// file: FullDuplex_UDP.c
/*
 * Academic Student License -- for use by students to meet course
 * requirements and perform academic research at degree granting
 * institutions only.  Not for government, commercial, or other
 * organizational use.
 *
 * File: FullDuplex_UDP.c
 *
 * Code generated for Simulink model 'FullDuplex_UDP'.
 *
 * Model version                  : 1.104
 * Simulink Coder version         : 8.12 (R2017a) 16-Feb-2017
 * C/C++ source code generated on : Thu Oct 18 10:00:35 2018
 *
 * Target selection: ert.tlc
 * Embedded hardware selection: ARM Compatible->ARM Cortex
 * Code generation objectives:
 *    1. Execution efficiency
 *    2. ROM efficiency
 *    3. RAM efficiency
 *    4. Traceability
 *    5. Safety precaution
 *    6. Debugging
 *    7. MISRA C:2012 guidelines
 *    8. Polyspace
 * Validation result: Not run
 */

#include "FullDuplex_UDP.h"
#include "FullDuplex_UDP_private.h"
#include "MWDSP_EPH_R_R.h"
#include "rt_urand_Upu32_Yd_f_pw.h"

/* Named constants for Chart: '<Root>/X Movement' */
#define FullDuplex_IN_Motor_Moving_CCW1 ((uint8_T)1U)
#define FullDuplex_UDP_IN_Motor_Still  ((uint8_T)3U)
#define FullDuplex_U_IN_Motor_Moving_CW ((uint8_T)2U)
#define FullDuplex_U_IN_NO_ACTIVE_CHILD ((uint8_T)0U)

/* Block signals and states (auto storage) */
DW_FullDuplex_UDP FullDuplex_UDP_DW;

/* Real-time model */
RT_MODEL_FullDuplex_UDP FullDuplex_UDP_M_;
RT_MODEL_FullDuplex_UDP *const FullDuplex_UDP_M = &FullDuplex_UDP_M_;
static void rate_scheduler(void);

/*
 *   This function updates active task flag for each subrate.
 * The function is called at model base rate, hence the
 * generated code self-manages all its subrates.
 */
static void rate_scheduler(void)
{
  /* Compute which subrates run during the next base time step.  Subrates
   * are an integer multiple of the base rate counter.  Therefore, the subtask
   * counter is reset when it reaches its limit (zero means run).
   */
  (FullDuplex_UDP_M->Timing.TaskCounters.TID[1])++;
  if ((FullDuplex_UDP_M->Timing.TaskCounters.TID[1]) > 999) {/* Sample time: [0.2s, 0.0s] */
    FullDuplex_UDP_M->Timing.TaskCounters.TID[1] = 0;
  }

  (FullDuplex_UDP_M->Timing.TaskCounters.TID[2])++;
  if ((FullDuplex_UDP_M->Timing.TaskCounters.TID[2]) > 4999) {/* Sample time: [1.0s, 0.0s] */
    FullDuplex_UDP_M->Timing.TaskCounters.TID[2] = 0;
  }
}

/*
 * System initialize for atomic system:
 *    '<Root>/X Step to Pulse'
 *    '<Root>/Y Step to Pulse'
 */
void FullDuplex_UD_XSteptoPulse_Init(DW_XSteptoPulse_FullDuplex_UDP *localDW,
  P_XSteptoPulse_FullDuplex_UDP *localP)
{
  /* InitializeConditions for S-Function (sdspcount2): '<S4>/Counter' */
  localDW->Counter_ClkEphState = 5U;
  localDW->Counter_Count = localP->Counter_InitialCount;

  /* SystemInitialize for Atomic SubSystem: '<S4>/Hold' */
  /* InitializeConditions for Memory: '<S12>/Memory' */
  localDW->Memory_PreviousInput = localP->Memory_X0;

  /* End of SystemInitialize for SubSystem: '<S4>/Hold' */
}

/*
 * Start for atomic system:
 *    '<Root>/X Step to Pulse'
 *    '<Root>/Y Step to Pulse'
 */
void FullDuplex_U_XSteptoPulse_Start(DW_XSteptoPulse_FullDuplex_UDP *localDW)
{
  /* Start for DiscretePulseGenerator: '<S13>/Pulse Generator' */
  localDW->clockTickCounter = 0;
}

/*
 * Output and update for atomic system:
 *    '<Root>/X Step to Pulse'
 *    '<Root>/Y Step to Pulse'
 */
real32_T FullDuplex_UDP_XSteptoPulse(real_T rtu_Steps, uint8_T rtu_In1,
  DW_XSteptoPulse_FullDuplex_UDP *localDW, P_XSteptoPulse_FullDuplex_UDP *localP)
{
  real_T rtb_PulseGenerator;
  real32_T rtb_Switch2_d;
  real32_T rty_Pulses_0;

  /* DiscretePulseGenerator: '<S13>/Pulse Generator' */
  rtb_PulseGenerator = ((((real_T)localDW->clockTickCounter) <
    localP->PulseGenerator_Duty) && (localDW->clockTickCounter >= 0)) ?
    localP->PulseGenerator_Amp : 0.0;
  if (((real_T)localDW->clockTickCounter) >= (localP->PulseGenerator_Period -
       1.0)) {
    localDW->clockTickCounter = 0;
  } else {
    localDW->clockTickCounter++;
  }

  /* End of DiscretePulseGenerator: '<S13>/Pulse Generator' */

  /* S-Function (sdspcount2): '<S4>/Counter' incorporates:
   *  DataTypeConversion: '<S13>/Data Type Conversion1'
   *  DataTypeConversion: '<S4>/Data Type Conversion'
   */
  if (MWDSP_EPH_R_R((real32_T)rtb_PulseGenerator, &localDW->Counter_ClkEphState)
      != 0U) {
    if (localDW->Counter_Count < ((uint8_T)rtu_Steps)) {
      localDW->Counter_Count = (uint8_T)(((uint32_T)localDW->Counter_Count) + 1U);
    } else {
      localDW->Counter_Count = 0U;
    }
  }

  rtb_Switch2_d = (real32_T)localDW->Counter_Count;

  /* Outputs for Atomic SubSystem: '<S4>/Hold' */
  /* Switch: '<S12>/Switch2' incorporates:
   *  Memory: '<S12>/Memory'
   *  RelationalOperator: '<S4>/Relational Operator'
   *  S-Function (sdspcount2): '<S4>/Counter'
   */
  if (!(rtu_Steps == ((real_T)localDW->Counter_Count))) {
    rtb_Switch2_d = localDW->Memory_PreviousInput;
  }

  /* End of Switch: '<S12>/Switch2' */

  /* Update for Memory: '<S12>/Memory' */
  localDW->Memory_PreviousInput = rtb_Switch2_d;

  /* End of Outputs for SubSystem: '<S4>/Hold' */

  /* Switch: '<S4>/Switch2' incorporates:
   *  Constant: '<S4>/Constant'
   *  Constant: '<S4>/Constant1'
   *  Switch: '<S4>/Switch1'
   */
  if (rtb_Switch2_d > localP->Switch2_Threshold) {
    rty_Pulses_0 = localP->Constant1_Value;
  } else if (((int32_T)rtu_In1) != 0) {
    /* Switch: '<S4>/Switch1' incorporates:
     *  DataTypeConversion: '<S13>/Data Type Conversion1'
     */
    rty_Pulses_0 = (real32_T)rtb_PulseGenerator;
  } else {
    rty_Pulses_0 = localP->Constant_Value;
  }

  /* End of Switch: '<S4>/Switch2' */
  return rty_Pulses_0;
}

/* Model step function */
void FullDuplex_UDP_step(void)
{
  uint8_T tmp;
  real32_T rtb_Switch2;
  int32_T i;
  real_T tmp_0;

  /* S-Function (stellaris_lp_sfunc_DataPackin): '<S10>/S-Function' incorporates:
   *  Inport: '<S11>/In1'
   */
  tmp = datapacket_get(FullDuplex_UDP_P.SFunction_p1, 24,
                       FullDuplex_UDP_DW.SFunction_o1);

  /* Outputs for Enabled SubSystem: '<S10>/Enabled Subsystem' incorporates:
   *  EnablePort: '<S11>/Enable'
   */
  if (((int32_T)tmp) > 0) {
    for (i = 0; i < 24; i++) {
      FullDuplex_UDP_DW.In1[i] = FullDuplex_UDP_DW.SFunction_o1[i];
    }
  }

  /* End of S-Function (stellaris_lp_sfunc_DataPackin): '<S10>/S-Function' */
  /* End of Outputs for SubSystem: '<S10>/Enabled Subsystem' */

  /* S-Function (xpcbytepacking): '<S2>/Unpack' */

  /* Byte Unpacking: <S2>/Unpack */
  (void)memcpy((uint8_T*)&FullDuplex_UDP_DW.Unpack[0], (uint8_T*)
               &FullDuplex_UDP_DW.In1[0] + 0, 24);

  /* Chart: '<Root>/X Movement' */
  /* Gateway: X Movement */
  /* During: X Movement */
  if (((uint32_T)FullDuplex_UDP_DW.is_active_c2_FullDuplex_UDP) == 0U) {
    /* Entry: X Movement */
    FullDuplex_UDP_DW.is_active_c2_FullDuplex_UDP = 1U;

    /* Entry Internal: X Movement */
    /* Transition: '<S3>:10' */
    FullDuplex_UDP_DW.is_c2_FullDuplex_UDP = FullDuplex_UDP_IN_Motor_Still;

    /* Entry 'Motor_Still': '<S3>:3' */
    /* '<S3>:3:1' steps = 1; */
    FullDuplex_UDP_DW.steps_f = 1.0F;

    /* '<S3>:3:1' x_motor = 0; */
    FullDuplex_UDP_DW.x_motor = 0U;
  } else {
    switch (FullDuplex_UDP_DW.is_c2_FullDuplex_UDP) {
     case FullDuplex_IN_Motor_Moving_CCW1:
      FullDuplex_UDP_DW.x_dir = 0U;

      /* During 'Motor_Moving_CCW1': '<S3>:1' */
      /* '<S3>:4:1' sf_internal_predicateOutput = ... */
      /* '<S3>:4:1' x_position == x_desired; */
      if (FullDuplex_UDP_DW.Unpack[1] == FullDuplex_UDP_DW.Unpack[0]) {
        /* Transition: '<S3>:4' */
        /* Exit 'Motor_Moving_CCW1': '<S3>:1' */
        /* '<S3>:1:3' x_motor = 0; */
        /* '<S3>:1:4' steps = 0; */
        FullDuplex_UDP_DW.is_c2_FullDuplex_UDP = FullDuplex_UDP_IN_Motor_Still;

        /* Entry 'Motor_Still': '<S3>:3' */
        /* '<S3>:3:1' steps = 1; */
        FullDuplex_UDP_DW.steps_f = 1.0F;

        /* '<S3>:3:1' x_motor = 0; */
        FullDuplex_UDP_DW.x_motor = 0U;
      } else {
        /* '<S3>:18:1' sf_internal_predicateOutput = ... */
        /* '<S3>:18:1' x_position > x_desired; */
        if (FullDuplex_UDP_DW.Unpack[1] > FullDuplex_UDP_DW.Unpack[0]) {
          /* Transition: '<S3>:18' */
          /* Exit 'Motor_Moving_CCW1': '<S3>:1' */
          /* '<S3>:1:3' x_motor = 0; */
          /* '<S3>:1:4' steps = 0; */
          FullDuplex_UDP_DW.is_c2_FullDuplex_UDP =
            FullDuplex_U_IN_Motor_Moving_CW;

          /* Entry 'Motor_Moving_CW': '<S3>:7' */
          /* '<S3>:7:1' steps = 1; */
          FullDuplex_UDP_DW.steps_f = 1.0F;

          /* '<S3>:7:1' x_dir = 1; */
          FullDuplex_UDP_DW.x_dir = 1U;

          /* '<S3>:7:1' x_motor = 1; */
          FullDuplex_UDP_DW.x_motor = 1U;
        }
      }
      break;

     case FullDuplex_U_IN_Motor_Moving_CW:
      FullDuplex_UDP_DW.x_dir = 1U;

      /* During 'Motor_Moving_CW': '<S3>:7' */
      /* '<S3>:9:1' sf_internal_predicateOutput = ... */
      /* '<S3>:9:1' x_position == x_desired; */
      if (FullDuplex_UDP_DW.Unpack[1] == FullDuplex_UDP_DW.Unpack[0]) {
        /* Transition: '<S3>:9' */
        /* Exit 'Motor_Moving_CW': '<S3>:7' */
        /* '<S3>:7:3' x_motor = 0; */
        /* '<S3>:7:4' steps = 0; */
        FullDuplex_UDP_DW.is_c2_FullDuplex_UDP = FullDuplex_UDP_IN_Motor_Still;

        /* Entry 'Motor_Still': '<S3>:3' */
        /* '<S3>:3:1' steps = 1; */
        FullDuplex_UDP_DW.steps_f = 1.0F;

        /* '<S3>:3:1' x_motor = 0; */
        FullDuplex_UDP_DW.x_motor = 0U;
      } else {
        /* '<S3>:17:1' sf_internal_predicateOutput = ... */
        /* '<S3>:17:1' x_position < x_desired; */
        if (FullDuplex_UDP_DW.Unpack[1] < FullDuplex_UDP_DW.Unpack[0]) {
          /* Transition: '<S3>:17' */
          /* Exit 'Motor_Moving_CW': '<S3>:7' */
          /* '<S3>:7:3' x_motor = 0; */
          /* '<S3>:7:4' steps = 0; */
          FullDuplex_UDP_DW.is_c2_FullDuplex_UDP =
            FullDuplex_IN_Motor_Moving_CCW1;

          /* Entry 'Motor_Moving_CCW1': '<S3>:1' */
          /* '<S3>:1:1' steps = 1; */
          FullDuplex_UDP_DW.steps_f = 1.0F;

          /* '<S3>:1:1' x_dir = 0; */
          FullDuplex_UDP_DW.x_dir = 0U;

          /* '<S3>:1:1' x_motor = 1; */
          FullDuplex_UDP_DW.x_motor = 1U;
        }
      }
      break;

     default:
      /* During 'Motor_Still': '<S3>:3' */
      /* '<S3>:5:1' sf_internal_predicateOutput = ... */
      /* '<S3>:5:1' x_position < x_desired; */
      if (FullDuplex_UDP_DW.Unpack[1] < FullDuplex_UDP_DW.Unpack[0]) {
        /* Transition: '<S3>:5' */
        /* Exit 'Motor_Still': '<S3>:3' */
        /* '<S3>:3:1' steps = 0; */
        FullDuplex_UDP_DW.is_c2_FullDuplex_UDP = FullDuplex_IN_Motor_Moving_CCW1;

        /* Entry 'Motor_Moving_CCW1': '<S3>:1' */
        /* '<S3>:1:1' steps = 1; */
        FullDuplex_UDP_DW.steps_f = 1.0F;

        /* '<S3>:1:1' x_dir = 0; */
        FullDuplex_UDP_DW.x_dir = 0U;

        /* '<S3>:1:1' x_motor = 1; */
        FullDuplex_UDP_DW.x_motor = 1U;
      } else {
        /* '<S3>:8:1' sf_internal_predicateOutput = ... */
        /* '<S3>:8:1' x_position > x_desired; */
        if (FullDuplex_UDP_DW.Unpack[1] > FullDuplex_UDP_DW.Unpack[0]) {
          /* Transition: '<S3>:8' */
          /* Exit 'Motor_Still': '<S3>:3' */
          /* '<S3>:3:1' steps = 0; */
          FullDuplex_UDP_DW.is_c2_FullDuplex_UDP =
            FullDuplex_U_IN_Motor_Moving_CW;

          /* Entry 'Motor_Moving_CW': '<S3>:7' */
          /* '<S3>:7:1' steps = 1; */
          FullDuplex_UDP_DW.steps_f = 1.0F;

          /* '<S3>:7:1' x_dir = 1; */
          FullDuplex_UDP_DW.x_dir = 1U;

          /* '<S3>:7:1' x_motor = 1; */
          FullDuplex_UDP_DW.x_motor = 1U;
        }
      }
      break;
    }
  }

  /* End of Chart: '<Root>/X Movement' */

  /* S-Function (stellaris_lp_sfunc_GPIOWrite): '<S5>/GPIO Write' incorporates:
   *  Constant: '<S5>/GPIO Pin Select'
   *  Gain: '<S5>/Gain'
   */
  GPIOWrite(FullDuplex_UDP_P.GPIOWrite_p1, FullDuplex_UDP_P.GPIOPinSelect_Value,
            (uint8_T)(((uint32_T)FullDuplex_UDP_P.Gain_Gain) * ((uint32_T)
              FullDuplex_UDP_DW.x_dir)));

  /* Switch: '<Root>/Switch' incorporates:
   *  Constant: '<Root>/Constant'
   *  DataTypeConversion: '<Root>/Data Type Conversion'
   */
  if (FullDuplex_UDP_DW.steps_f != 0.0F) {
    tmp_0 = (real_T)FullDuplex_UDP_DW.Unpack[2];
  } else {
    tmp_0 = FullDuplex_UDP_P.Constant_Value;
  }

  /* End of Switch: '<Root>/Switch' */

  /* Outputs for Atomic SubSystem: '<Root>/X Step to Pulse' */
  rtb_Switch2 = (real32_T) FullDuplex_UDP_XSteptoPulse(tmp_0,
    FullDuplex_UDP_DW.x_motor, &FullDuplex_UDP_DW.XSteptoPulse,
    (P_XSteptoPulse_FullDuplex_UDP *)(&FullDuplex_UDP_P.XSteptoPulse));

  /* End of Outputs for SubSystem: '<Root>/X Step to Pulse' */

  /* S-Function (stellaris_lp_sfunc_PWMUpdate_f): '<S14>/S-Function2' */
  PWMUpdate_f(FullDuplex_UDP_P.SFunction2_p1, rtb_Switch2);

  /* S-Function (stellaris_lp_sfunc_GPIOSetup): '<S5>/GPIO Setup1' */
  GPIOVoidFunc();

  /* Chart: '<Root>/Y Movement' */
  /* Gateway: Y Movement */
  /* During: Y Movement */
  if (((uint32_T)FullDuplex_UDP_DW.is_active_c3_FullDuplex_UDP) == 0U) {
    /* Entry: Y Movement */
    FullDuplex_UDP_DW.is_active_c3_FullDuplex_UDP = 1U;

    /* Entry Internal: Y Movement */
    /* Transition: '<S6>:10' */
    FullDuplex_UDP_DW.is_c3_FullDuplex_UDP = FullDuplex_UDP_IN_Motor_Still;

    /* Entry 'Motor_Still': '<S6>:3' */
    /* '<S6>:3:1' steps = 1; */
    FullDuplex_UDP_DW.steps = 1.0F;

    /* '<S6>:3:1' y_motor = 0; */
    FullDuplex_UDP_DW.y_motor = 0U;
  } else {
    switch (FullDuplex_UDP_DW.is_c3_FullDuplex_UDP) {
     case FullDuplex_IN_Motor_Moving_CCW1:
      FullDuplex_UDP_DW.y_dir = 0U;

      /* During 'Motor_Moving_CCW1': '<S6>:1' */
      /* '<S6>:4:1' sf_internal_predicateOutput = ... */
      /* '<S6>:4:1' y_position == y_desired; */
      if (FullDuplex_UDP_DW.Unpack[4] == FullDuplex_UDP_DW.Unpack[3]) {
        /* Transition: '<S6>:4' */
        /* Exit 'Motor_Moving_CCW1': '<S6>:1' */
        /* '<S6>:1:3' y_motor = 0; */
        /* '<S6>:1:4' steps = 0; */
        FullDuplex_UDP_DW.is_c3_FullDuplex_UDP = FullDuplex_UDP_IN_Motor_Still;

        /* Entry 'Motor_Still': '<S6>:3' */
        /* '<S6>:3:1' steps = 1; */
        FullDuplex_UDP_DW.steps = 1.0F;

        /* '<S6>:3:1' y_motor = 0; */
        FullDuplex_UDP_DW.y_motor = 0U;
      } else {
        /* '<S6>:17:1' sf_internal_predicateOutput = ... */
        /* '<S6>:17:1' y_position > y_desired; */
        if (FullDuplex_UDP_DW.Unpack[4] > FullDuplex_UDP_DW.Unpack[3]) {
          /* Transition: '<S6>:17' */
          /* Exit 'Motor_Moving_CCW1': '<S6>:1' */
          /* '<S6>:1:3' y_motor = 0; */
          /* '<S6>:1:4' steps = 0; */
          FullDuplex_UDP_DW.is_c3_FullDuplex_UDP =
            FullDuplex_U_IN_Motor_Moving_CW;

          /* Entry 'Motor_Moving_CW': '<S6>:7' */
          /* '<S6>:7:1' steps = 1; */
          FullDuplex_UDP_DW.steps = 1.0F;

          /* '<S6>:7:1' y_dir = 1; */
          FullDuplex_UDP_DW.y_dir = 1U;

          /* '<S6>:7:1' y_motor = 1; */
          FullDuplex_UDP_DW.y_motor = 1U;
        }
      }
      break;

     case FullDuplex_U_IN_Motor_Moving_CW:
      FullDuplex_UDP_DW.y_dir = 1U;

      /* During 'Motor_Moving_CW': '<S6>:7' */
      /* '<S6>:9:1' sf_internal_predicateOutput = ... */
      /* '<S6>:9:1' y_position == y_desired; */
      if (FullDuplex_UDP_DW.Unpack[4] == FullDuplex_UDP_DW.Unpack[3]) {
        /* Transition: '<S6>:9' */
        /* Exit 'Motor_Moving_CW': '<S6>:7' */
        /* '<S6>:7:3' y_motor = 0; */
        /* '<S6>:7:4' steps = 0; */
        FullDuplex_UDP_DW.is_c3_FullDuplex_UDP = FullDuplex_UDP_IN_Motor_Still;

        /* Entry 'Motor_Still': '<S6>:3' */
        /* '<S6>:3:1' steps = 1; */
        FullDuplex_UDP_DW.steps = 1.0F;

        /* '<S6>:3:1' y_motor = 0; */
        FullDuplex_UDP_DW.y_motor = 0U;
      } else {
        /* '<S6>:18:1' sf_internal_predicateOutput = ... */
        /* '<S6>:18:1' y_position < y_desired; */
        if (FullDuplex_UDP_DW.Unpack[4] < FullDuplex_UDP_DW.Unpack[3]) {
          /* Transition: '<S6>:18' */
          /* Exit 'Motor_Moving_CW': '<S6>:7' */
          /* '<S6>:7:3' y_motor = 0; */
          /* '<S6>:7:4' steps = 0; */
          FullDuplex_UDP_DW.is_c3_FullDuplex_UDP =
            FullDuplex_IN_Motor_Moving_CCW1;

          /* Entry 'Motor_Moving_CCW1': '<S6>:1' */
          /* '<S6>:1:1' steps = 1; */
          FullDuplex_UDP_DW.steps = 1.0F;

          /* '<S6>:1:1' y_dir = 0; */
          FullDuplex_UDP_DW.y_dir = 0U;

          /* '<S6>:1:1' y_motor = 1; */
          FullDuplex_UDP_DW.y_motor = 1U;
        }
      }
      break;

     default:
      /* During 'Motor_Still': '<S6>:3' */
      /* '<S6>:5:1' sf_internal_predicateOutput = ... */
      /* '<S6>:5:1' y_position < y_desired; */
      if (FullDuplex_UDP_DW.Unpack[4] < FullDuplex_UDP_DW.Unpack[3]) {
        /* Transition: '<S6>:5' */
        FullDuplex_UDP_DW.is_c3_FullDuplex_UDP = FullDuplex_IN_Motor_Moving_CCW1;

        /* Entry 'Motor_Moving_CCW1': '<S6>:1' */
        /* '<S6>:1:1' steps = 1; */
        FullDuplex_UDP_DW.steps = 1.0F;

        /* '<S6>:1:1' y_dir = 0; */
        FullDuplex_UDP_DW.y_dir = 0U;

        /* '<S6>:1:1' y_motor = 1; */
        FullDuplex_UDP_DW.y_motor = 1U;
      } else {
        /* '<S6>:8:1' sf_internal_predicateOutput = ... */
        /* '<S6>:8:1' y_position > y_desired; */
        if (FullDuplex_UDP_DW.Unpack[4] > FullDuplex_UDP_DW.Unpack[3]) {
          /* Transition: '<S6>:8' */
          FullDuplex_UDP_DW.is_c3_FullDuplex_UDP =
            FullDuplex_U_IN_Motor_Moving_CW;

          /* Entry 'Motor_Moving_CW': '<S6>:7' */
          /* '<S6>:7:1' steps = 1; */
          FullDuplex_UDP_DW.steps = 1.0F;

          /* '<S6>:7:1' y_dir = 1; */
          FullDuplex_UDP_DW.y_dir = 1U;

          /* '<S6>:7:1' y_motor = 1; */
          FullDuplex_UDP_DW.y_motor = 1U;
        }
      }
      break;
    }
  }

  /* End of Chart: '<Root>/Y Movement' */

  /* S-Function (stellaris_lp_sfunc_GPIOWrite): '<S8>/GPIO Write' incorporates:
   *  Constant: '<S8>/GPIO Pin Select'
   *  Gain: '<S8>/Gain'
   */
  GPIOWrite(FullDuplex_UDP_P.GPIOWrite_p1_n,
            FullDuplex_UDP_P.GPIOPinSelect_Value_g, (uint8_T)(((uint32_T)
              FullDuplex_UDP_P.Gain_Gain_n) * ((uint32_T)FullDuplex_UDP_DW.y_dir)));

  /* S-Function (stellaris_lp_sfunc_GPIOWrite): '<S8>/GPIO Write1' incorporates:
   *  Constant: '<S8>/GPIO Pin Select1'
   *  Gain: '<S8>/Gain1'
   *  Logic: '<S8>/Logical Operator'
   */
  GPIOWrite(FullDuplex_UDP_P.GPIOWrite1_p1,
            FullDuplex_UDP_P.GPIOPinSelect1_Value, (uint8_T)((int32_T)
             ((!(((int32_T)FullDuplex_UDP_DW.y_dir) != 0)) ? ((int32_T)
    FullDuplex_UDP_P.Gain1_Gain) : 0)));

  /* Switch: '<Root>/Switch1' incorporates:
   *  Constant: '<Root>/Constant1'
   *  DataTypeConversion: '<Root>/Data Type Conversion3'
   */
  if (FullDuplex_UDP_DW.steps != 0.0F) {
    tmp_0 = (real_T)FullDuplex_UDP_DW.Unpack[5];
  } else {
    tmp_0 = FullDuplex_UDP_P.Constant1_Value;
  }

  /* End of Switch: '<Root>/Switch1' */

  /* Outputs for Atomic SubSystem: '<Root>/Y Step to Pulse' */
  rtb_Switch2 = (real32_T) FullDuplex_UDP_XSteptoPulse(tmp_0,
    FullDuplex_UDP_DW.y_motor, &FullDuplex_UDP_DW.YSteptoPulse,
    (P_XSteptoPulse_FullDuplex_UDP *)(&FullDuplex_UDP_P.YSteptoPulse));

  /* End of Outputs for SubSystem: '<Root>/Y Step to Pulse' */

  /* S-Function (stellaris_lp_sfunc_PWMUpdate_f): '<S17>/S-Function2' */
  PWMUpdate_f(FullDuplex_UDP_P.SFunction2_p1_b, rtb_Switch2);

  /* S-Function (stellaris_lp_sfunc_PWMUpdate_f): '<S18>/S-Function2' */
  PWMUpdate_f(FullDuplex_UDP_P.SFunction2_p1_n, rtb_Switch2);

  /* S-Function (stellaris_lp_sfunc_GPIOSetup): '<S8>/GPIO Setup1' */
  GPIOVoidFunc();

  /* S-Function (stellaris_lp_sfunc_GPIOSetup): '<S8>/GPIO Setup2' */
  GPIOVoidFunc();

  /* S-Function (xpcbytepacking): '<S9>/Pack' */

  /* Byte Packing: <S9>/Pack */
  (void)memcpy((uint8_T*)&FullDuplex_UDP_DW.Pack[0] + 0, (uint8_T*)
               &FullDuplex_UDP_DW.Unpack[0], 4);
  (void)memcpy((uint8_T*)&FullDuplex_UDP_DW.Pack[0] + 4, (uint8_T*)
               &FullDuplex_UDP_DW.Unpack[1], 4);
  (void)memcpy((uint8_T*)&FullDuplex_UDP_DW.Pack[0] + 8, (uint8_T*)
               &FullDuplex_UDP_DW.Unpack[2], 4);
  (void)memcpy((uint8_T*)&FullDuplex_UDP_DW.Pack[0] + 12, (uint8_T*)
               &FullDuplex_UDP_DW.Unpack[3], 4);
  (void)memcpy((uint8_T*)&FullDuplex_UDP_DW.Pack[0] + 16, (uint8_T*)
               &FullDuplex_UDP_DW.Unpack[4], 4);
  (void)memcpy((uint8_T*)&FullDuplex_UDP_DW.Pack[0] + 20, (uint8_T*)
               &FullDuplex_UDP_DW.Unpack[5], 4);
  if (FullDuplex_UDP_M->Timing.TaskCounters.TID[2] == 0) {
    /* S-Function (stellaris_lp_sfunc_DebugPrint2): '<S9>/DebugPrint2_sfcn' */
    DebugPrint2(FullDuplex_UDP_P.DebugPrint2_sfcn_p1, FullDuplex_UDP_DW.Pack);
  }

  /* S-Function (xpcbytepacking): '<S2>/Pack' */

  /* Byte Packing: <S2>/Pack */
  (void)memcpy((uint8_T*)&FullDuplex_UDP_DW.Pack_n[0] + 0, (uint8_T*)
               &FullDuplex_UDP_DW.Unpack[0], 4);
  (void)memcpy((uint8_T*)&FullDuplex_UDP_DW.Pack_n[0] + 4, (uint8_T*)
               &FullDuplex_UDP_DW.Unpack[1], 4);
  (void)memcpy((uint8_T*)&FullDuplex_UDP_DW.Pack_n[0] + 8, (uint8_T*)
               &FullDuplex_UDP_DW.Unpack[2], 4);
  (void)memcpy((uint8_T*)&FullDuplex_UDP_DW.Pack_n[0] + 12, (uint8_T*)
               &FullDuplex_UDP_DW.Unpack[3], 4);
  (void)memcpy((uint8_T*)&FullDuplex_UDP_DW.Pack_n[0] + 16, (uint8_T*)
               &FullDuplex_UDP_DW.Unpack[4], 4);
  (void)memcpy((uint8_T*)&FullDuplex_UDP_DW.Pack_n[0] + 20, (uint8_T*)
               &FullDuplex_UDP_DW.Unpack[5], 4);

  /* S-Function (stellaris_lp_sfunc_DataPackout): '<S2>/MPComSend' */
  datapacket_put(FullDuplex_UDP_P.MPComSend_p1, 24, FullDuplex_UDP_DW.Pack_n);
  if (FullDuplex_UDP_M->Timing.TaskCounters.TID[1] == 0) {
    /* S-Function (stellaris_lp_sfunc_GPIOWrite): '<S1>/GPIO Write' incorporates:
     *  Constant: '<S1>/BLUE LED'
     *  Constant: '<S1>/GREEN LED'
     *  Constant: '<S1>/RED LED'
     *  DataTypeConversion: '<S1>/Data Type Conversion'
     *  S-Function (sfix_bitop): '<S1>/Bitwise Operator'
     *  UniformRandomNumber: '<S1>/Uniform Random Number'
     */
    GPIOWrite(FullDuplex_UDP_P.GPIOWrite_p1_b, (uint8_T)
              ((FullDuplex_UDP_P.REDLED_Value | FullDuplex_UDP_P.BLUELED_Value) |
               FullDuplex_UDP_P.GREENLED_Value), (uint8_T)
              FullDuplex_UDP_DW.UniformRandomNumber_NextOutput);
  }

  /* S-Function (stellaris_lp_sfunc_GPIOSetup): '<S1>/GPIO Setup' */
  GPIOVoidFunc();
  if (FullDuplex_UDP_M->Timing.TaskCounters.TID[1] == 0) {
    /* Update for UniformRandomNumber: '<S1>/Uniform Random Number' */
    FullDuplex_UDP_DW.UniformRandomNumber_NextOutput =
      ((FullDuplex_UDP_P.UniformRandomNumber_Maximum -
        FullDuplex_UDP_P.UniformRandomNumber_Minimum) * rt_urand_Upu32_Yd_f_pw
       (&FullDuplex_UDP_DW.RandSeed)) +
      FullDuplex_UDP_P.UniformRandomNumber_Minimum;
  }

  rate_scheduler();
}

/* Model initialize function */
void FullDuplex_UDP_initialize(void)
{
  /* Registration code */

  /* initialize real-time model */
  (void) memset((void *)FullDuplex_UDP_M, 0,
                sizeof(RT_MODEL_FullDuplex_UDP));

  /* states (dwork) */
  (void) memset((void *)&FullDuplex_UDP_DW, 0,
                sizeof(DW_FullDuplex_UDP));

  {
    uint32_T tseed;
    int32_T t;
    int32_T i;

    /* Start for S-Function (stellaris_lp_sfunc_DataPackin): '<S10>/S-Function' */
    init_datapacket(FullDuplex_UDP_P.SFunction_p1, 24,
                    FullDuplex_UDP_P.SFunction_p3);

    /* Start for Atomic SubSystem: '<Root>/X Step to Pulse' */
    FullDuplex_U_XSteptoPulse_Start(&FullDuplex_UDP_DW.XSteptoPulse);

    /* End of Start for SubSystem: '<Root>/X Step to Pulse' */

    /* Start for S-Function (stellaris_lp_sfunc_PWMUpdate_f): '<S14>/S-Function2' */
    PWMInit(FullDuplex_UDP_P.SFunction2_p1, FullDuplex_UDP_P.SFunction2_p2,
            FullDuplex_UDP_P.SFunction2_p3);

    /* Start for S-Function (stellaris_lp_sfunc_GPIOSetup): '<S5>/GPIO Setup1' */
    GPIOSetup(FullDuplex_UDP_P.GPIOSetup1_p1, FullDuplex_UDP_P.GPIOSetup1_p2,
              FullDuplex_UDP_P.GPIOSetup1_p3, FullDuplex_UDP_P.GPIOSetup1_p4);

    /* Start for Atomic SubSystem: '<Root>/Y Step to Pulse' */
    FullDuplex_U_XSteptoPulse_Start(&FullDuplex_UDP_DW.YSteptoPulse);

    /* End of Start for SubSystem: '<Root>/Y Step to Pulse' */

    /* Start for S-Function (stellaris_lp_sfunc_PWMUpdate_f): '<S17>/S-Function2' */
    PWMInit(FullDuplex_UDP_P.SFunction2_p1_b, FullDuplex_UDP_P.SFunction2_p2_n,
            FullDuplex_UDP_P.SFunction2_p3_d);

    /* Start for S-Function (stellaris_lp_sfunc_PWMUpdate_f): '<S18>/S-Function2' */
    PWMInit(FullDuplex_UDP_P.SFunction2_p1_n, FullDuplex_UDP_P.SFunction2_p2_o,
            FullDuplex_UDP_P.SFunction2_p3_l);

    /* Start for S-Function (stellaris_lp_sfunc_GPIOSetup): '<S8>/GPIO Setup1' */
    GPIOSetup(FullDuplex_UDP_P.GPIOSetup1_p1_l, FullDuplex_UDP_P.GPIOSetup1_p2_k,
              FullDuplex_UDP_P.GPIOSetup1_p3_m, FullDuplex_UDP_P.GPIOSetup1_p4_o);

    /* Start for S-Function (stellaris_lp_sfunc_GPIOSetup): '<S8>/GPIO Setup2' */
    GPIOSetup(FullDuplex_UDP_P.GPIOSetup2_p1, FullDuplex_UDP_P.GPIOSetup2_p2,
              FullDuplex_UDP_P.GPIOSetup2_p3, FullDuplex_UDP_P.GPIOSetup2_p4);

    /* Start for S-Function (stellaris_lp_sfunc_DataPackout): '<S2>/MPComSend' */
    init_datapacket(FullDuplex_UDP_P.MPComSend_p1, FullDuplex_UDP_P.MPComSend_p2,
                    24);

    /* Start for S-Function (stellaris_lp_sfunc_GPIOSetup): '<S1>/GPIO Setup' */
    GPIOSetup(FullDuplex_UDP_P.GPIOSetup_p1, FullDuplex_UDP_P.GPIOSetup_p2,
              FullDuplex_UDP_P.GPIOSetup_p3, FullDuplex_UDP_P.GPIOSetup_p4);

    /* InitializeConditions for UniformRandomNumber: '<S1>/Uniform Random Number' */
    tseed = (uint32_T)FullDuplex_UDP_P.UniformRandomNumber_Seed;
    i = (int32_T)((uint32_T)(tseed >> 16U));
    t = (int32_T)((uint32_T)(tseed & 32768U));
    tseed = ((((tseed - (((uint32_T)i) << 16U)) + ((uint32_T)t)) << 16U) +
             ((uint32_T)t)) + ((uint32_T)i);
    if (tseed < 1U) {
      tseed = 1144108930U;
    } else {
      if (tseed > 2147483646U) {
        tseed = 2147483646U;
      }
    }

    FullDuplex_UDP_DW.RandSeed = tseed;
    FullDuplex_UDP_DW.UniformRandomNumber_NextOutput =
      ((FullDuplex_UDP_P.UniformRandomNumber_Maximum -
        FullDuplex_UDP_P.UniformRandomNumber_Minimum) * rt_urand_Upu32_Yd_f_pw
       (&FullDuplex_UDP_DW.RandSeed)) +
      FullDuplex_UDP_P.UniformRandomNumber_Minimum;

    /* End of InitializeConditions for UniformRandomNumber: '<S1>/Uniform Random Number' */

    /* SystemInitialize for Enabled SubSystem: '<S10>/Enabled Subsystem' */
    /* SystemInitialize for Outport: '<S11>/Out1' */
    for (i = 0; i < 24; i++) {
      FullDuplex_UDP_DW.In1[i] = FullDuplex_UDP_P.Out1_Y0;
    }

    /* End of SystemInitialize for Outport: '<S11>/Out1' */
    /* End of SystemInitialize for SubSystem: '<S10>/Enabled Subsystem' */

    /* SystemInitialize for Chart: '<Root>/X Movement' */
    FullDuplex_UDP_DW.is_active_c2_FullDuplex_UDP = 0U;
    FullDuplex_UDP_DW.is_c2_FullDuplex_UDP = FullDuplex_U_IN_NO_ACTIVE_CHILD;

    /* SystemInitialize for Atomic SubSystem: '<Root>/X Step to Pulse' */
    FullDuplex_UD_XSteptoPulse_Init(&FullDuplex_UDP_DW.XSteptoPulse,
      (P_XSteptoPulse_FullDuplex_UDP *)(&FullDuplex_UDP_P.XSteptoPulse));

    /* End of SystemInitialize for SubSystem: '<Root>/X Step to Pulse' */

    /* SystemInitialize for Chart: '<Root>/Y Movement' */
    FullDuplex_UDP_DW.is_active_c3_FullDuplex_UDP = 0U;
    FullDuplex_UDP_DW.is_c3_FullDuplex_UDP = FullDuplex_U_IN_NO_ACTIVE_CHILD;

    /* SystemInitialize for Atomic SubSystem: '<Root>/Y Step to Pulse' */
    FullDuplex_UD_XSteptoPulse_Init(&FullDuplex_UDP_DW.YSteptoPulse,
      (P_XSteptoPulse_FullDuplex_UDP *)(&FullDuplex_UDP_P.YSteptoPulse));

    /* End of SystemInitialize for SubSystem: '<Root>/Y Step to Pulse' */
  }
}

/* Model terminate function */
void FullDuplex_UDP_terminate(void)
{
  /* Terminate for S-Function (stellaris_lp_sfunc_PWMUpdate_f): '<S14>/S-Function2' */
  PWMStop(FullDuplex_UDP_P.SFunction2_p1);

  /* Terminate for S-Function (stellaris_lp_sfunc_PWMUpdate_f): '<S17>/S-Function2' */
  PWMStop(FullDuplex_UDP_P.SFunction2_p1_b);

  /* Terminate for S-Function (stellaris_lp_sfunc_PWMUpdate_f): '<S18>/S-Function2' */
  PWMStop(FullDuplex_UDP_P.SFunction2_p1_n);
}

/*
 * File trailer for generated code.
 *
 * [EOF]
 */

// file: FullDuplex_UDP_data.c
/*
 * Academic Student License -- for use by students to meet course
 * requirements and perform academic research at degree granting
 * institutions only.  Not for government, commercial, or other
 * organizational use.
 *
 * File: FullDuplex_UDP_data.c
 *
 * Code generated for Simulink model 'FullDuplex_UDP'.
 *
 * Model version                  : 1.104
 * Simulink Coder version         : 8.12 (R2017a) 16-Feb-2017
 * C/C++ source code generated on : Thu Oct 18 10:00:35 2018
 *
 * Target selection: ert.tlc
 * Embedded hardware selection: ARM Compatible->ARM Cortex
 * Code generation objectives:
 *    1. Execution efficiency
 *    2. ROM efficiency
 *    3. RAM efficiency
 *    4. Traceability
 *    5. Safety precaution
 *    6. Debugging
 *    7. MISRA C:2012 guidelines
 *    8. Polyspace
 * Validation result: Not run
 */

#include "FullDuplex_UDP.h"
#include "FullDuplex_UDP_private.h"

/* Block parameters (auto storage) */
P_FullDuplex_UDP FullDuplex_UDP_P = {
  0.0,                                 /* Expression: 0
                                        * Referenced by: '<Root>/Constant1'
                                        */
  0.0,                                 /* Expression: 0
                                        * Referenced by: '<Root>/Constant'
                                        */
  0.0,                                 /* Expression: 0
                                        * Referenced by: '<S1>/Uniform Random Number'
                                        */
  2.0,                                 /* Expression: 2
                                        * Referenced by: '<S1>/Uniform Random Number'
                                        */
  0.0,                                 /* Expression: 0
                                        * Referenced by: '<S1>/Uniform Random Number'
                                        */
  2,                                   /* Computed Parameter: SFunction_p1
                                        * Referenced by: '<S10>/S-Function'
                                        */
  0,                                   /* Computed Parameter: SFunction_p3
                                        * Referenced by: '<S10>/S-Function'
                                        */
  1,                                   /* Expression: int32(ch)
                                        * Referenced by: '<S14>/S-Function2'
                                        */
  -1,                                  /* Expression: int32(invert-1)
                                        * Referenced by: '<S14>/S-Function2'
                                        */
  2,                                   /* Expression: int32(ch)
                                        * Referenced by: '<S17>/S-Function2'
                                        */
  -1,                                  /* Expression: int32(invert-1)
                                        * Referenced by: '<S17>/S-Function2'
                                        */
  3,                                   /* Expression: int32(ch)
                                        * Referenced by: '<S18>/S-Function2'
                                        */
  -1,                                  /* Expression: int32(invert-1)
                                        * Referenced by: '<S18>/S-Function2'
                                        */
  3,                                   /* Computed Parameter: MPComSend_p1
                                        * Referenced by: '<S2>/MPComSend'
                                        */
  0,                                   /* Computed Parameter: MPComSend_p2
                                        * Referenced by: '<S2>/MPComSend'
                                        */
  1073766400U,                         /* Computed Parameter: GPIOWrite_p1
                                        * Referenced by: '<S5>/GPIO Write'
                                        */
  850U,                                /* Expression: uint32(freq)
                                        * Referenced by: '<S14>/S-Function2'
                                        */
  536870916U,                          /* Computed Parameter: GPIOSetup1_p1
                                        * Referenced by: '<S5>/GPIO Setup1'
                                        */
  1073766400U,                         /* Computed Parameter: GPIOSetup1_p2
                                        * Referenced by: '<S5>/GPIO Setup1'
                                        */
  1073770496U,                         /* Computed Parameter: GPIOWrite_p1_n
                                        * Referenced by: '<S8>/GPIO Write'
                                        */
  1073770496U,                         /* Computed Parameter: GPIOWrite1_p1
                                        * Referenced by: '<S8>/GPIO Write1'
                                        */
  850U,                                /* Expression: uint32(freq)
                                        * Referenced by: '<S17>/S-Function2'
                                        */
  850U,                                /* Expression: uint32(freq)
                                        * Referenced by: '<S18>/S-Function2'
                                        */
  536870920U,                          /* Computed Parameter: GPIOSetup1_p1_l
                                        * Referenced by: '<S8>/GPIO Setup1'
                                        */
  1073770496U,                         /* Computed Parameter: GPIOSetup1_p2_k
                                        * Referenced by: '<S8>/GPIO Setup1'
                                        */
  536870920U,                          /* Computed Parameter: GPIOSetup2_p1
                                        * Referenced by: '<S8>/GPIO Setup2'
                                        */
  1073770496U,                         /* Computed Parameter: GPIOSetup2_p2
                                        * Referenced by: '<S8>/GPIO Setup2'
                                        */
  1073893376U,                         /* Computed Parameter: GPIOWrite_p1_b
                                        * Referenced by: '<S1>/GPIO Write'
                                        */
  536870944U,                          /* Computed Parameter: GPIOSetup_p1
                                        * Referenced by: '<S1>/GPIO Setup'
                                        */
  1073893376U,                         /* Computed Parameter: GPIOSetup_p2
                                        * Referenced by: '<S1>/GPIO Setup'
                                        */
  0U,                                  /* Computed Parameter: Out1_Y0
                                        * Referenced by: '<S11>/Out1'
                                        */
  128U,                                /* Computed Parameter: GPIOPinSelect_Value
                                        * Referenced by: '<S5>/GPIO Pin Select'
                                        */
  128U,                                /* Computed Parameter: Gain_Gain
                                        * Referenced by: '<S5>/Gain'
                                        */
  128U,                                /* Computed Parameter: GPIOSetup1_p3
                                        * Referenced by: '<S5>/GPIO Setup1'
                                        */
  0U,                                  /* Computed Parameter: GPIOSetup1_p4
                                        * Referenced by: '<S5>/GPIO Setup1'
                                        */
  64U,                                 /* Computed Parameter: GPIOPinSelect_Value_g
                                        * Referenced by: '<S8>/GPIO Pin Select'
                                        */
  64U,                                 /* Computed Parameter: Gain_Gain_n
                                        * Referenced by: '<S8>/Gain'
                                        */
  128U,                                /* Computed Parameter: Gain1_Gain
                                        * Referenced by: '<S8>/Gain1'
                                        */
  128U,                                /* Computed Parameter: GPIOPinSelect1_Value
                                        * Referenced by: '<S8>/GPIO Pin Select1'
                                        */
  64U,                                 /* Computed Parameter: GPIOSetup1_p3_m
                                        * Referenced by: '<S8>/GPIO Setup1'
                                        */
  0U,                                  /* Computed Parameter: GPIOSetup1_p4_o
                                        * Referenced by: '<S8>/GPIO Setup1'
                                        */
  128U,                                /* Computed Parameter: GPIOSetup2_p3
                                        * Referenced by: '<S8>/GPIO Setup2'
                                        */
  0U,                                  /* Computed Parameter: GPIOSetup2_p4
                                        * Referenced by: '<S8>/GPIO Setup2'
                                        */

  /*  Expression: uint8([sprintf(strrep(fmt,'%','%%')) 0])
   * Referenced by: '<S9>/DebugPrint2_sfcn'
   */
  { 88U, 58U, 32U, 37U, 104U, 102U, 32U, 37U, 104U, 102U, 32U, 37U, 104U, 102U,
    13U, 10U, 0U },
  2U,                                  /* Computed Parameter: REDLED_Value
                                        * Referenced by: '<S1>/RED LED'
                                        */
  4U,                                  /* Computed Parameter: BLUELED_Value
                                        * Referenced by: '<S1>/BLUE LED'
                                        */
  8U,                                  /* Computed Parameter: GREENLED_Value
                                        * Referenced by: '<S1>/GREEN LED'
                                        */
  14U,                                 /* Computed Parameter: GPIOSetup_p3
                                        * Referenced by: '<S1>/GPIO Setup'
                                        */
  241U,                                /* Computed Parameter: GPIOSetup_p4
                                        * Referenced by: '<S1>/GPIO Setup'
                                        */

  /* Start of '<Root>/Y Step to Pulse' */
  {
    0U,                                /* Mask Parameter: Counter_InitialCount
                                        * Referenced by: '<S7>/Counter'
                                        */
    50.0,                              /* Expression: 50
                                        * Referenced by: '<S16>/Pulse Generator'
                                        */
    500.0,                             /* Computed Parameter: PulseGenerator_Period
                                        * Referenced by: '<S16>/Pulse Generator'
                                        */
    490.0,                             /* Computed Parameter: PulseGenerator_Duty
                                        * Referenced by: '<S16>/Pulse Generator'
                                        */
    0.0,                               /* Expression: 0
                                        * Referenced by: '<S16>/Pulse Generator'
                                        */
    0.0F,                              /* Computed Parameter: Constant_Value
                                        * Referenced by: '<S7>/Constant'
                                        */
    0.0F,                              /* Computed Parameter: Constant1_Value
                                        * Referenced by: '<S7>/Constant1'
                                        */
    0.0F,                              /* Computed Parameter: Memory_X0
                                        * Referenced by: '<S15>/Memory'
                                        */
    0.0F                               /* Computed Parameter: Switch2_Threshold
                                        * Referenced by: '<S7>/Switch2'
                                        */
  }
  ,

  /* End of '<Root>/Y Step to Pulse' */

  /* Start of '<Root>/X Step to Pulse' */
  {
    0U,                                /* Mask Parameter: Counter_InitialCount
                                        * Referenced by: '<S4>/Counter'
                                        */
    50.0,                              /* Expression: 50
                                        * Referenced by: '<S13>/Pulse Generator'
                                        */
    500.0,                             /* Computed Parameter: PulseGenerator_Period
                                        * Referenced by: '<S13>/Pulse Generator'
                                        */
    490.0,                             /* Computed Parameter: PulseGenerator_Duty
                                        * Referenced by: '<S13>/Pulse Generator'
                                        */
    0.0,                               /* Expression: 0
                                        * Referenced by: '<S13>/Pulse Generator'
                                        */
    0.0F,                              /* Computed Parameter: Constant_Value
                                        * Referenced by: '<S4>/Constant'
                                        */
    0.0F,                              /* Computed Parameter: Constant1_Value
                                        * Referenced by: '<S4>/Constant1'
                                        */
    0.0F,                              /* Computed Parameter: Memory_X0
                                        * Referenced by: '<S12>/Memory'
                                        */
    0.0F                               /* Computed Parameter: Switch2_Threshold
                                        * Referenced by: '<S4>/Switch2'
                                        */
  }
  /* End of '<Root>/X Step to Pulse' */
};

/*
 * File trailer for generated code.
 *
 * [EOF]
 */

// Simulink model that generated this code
simulink model "FullDuplex_UDP"  (R2017a)
settings: Solver=FixedStepDiscrete  StartTime=0.0  StopTime=10.0  FixedStep=0.0002  RelTol=1e-3
libraries: stellaris_lp_lib x20, simulink x4, xpcutilitieslib x2, dspswit3 x2

== system FullDuplex_UDP ==
  Constant : Constant  Value=0
  Constant1 : Constant  Value=0
  Data Type Conversion{,1..5} (6 alike) : DataTypeConversion
  Running Indicator1 : Subsystem
  Switch : Switch  Criteria=u2 ~= 0
  Switch1 : Switch  Criteria=u2 ~= 0
  UDP RECEIVE : Subsystem
  X Movement : Stateflow chart  TreatAsAtomicUnit=on
  X Step to Pulse : Subsystem  TreatAsAtomicUnit=on
  X-Axis : Subsystem
  Y Movement : Stateflow chart  TreatAsAtomicUnit=on
  Y Step to Pulse : Subsystem  TreatAsAtomicUnit=on
  Y-Axis : Subsystem
  wires:
  UDP RECEIVE/3(X-Steps) -> Data Type Conversion/1
  Data Type Conversion2/1 -> X Movement/2(x_desired)
  Data Type Conversion1/1 -> X Movement/1(x_position)
  UDP RECEIVE/1("Direction-1 ") -> Data Type Conversion2/1
  UDP RECEIVE/2("Direction-2 ") -> Data Type Conversion1/1
  Y Movement/2(y_dir) -> Y-Axis/1(Direction)
  Y Step to Pulse/1(Pulses) -> Y-Axis/2(Speed (%))
  X Movement/2(x_dir) -> X-Axis/1(Direction)
  Y Movement/1(y_motor) -> Y Step to Pulse/2(In1)
  X Movement/1(x_motor) -> X Step to Pulse/2(In1)
  X Step to Pulse/1(Pulses) -> X-Axis/2(Speed (%))
  UDP RECEIVE/4("Direction-3 ") -> Data Type Conversion5/1
  Data Type Conversion5/1 -> Y Movement/2(y_desired)
  UDP RECEIVE/5("Direction-4 ") -> Data Type Conversion4/1
  Data Type Conversion4/1 -> Y Movement/1(y_position)
  UDP RECEIVE/6(Y-Steps) -> Data Type Conversion3/1
  Data Type Conversion/1 -> Switch/1
  Constant/1 -> Switch/3
  X Movement/3(steps) -> Switch/2
  Switch/1 -> X Step to Pulse/1(Steps)
  Y Movement/3(steps) -> Switch1/2
  Constant1/1 -> Switch1/3
  Switch1/1 -> Y Step to Pulse/1(Steps)
  Data Type Conversion3/1 -> Switch1/1

== system FullDuplex_UDP/Running Indicator1 ==
  BLUE LED : stellaris_lp_lib/GPIO/GPIO Pin Select  GPIO_PIN_X=GPIO_PIN_2
  Bitwise Operator : simulink/Logic and Bit Operations/Bitwise Operator  logicop=OR  UseBitMask=off  NumInputPorts=3  BitMask=bin2dec('11011001')  BitMaskRealWorld=Stored Integer
  Data Type Conversion : DataTypeConversion
  GPIO Setup : stellaris_lp_lib/GPIO/GPIO Setup  GPIO_PORTX_BASE=GPIO_PORTF_BASE  PinsOutput_0=Input  PinsOutput_1=Output  PinsOutput_2=Output  PinsOutput_3=Output  PinsOutput_4=Input  PinsOutput_5=Input  PinsOutput_6=Input  PinsOutput_7=Input
  GPIO Write : stellaris_lp_lib/GPIO/GPIO Write  GPIO_PORTX_BASE=GPIO_PORTF_BASE  SampleTime=-1
  GREEN LED : stellaris_lp_lib/GPIO/GPIO Pin Select  GPIO_PIN_X=GPIO_PIN_3
  RED LED : stellaris_lp_lib/GPIO/GPIO Pin Select  GPIO_PIN_X=GPIO_PIN_1
  Uniform Random Number : UniformRandomNumber  Minimum=0  Maximum=2  SampleTime=0.2
  wires:
  BLUE LED/1 -> Bitwise Operator/2
  RED LED/1 -> Bitwise Operator/1
  GREEN LED/1 -> Bitwise Operator/3
  Bitwise Operator/1 -> GPIO Write/1
  Uniform Random Number/1 -> Data Type Conversion/1
  Data Type Conversion/1 -> GPIO Write/2

== system FullDuplex_UDP/UDP RECEIVE ==
  Advanced Debug Print : stellaris_lp_lib/Debug/Advanced Debug Print  types={'single','single','single','single','single','single'}  fmt='X: %hf %hf %hf\r\n'  sample_time=1
  Demux : Demux  Outputs=6
  MPComRecv : stellaris_lp_lib/Communication/MPComRecv  vport=2  pack_size=24  sample_time=-1
  MPComSend : stellaris_lp_lib/Communication/MPComSend  vport=3  pack_size=24  sample_time=-1
  Pack : xpcutilitieslib/Byte Packing   MaskPackedDataType=uint8  MaskUnpackedDataTypes={'single','single','single','single','single','single'}  MaskAlignment=1
  Unpack : xpcutilitieslib/Byte Unpacking   MaskUnpackedDataTypes={['single']}  MaskUnpackedDataSizes={[1,6]}  MaskAlignment=1
  "Direction-1 " : Outport
  "Direction-2 " : Outport  Port=2
  X-Steps : Outport  Port=3
  "Direction-3 " : Outport  Port=4
  "Direction-4 " : Outport  Port=5
  Y-Steps : Outport  Port=6
  wires:
  Demux/1 -> Advanced Debug Print/1, "Direction-1 "/1, Pack/1
  Demux/2 -> Advanced Debug Print/2, "Direction-2 "/1, Pack/2
  Pack/1 -> MPComSend/1
  MPComRecv/1 -> Unpack/1
  Unpack/1 -> Demux/1
  Demux/3 -> Pack/3, X-Steps/1, Advanced Debug Print/3
  Demux/4 -> "Direction-3 "/1, Advanced Debug Print/4, Pack/4
  Demux/5 -> Pack/5, "Direction-4 "/1, Advanced Debug Print/5
  Demux/6 -> Pack/6, Y-Steps/1, Advanced Debug Print/6

== system FullDuplex_UDP/X Step to Pulse ==
  Steps : Inport
  In1 : Inport  Port=2
  Constant : Constant  Value=0  OutDataTypeStr=single
  Constant1 : Constant  Value=0  OutDataTypeStr=single
  Counter : dspswit3/Counter  Direction=Up  CountEvent=Rising edge  CounterSize=Specify via input port  MaxCount=255  InitialCount=0  Output=Count  HitValue=2  ResetInput=off  SamplesPerFrame=1  Ts=1  CntDtype=single  HitDtype=Logical
  Data Type Conversion : DataTypeConversion  OutDataTypeStr=uint8
  Hold : Subsystem  TreatAsAtomicUnit=on
  PWM2 : Subsystem
  Relational Operator : RelationalOperator  Operator===  OutDataTypeStr=boolean  RndMeth=Simplest
  Scope : Scope
  Scope1 : Scope
  Scope2 : Scope
  Switch1 : Switch  Criteria=u2 ~= 0
  Switch2 : Switch  Criteria=u2 > Threshold
  Pulses : Outport
  wires:
  Steps/1 -> Relational Operator/1, Data Type Conversion/1
  Data Type Conversion/1 -> Counter/2
  Relational Operator/1 -> Hold/2(Hold)
  Switch1/1 -> Scope1/1, Switch2/3
  Counter/1 -> Hold/1(u), Relational Operator/2
  PWM2/1(PWM) -> Scope/1, Switch1/1, Counter/1
  In1/1 -> Scope2/1, Switch1/2
  Constant/1 -> Switch1/3
  Switch2/1 -> Pulses/1
  Constant1/1 -> Switch2/1
  Hold/1(y) -> Switch2/2

== system FullDuplex_UDP/X-Axis ==
  Direction : Inport  OutDataTypeStr=uint8
  Speed (%) : Inport  Port=2  OutDataTypeStr=single
  Bitwise Operator : simulink/Logic and Bit Operations/Bitwise Operator  logicop=OR  UseBitMask=off  BitMask=bin2dec('11011001')  BitMaskRealWorld=Real World Value
  GPIO Pin Select : stellaris_lp_lib/GPIO/GPIO Pin Select  GPIO_PIN_X=GPIO_PIN_7
  GPIO Setup1 : stellaris_lp_lib/GPIO/GPIO Setup  GPIO_PORTX_BASE=GPIO_PORTC_BASE  PinsOutput_0=Unused  PinsOutput_1=Unused  PinsOutput_2=Unused  PinsOutput_3=Unused  PinsOutput_4=Unused  PinsOutput_5=Unused  PinsOutput_6=Unused  PinsOutput_7=Output
  GPIO Write : stellaris_lp_lib/GPIO/GPIO Write  GPIO_PORTX_BASE=GPIO_PORTC_BASE  SampleTime=-1
  Gain : Gain  Gain=128  ParamDataTypeStr=uint8  OutDataTypeStr=uint8
  PWM Output X-Axis : stellaris_lp_lib/PWM/PWM Output  ch="1    PC4"  invert=off  freq=900  sample_time=-1
  Scope : Scope
  wires:
  Direction/1 -> Gain/1
  GPIO Pin Select/1 -> Bitwise Operator/1
  Bitwise Operator/1 -> GPIO Write/1
  Gain/1 -> GPIO Write/2
  Speed (%)/1 -> Scope/1, PWM Output X-Axis/1

== system FullDuplex_UDP/Y Step to Pulse ==
  Steps : Inport
  In1 : Inport  Port=2
  Constant : Constant  Value=0  OutDataTypeStr=single
  Constant1 : Constant  Value=0  OutDataTypeStr=single
  Counter : dspswit3/Counter  Direction=Up  CountEvent=Rising edge  CounterSize=Specify via input port  MaxCount=255  InitialCount=0  Output=Count  HitValue=2  ResetInput=off  SamplesPerFrame=1  Ts=1  CntDtype=single  HitDtype=Logical
  Data Type Conversion : DataTypeConversion  OutDataTypeStr=uint8
  Hold : Subsystem  TreatAsAtomicUnit=on
  PWM2 : Subsystem
  Relational Operator : RelationalOperator  Operator===  OutDataTypeStr=boolean  RndMeth=Simplest
  Scope : Scope
  Scope1 : Scope
  Scope2 : Scope
  Switch1 : Switch  Criteria=u2 ~= 0
  Switch2 : Switch  Criteria=u2 > Threshold
  Pulses : Outport
  wires:
  Steps/1 -> Relational Operator/1, Data Type Conversion/1
  Data Type Conversion/1 -> Counter/2
  Relational Operator/1 -> Hold/2(Hold)
  Switch1/1 -> Scope1/1, Switch2/3
  Counter/1 -> Hold/1(u), Relational Operator/2
  PWM2/1(PWM) -> Scope/1, Switch1/1, Counter/1
  In1/1 -> Scope2/1, Switch1/2
  Constant/1 -> Switch1/3
  Switch2/1 -> Pulses/1
  Constant1/1 -> Switch2/1
  Hold/1(y) -> Switch2/2

== system FullDuplex_UDP/Y-Axis ==
  Direction : Inport  OutDataTypeStr=uint8
  Speed (%) : Inport  Port=2  OutDataTypeStr=single
  Bitwise Operator : simulink/Logic and Bit Operations/Bitwise Operator  logicop=OR  UseBitMask=off  BitMask=bin2dec('11011001')  BitMaskRealWorld=Real World Value
  Bitwise Operator1 : simulink/Logic and Bit Operations/Bitwise Operator  logicop=OR  UseBitMask=off  BitMask=bin2dec('11011001')  BitMaskRealWorld=Real World Value
  GPIO Pin Select : stellaris_lp_lib/GPIO/GPIO Pin Select  GPIO_PIN_X=GPIO_PIN_6
  GPIO Pin Select1 : stellaris_lp_lib/GPIO/GPIO Pin Select  GPIO_PIN_X=GPIO_PIN_7
  GPIO Setup1 : stellaris_lp_lib/GPIO/GPIO Setup  GPIO_PORTX_BASE=GPIO_PORTD_BASE  PinsOutput_0=Unused  PinsOutput_1=Unused  PinsOutput_2=Unused  PinsOutput_3=Unused  PinsOutput_4=Unused  PinsOutput_5=Unused  PinsOutput_6=Output  PinsOutput_7=Unused
  GPIO Setup2 : stellaris_lp_lib/GPIO/GPIO Setup  GPIO_PORTX_BASE=GPIO_PORTD_BASE  PinsOutput_0=Unused  PinsOutput_1=Unused  PinsOutput_2=Unused  PinsOutput_3=Unused  PinsOutput_4=Unused  PinsOutput_5=Unused  PinsOutput_6=Unused  PinsOutput_7=Output
  GPIO Write : stellaris_lp_lib/GPIO/GPIO Write  GPIO_PORTX_BASE=GPIO_PORTD_BASE  SampleTime=-1
  GPIO Write1 : stellaris_lp_lib/GPIO/GPIO Write  GPIO_PORTX_BASE=GPIO_PORTD_BASE  SampleTime=-1
  Gain : Gain  Gain=64  ParamDataTypeStr=uint8  OutDataTypeStr=uint8
  Gain1 : Gain  Gain=128  OutDataTypeStr=uint8
  Logical Operator : Logic  Operator=NOT  AllPortsSameDT=off  OutDataTypeStr=boolean
  PWM Output Y-Axis (Left) : stellaris_lp_lib/PWM/PWM Output  ch="2    PC5"  invert=off  freq=900  sample_time=-1
  PWM Output Y-Axis (Right) : stellaris_lp_lib/PWM/PWM Output  ch="3    PC6"  invert=off  freq=900  sample_time=-1
  wires:
  Gain1/1 -> GPIO Write1/2
  Gain/1 -> GPIO Write/2
  Bitwise Operator1/1 -> GPIO Write1/1
  GPIO Pin Select1/1 -> Bitwise Operator1/1
  Speed (%)/1 -> PWM Output Y-Axis (Left)/1, PWM Output Y-Axis (Right)/1
  Logical Operator/1 -> Gain1/1
  Bitwise Operator/1 -> GPIO Write/1
  GPIO Pin Select/1 -> Bitwise Operator/1
  Direction/1 -> Logical Operator/1, Gain/1

== system FullDuplex_UDP/X Step to Pulse/Hold ==
  u : Inport  OutDataTypeStr=single
  Hold : Inport  Port=2  OutDataTypeStr=boolean
  Memory : Memory
  Switch2 : Switch  Criteria=u2 > Threshold  OutDataTypeStr=single
  y : Outport  OutDataTypeStr=single
  wires:
  u/1 -> Switch2/1
  Switch2/1 -> Memory/1, y/1
  Memory/1 -> Switch2/3
  Hold/1 -> Switch2/2

== system FullDuplex_UDP/X Step to Pulse/PWM2 ==
  Data Type Conversion1 : DataTypeConversion  OutDataTypeStr=single
  Pulse Generator : DiscretePulseGenerator  PulseType=Time based  Amplitude=50  Period=.1  PulseWidth=98
  PWM : Outport
  wires:
  Pulse Generator/1 -> Data Type Conversion1/1
  Data Type Conversion1/1 -> PWM/1

== system FullDuplex_UDP/Y Step to Pulse/Hold ==
  u : Inport  OutDataTypeStr=single
  Hold : Inport  Port=2  OutDataTypeStr=boolean
  Memory : Memory
  Switch2 : Switch  Criteria=u2 > Threshold  OutDataTypeStr=single
  y : Outport  OutDataTypeStr=single
  wires:
  u/1 -> Switch2/1
  Switch2/1 -> Memory/1, y/1
  Memory/1 -> Switch2/3
  Hold/1 -> Switch2/2

== system FullDuplex_UDP/Y Step to Pulse/PWM2 ==
  Data Type Conversion1 : DataTypeConversion  OutDataTypeStr=single
  Pulse Generator : DiscretePulseGenerator  PulseType=Time based  Amplitude=50  Period=.1  PulseWidth=98
  PWM : Outport
  wires:
  Pulse Generator/1 -> Data Type Conversion1/1
  Data Type Conversion1/1 -> PWM/1

== stateflow chart FullDuplex_UDP/X Movement ==
  state Motor_Moving_CCW1
    entry:
    steps = 1;
    x_dir = 0;
    x_motor = 1;
    exit:
    x_motor = 0;
    steps = 0;
  state Motor_Still
    entry:
    steps = 1;
    x_motor = 0;
    exit:
    steps = 0;
  state Motor_Moving_CW
    entry:
    steps = 1;
    x_dir = 1;
    x_motor = 1;
    exit:
    x_motor = 0;
    steps = 0;
  (default) -> Motor_Still
  Motor_Still -> Motor_Moving_CCW1 [order 1] : [x_position < x_desired]
  Motor_Moving_CCW1 -> Motor_Still [order 1] : [x_position == x_desired]
  Motor_Moving_CW -> Motor_Still [order 1] : [x_position == x_desired]
  Motor_Still -> Motor_Moving_CW [order 2] : [x_position > x_desired]
  Motor_Moving_CCW1 -> Motor_Moving_CW [order 2] : [x_position > x_desired]
  Motor_Moving_CW -> Motor_Moving_CCW1 [order 2] : [x_position < x_desired]
  data: x_position input; x_desired input; x_motor output uint8; x_dir output uint8; steps output single

== stateflow chart FullDuplex_UDP/Y Movement ==
  state Motor_Still
    entry:
    steps = 1;
    y_motor = 0;
  state Motor_Moving_CCW1
    entry:
    steps = 1;
    y_dir = 0;
    y_motor = 1;
    exit:
    y_motor = 0;
    steps = 0;
  state Motor_Moving_CW
    entry:
    steps = 1;
    y_dir = 1;
    y_motor = 1;
    exit:
    y_motor = 0;
    steps = 0;
  (default) -> Motor_Still
  Motor_Still -> Motor_Moving_CCW1 [order 1] : [y_position < y_desired]
  Motor_Moving_CCW1 -> Motor_Still [order 1] : [y_position == y_desired]
  Motor_Moving_CW -> Motor_Still [order 1] : [y_position == y_desired]
  Motor_Still -> Motor_Moving_CW [order 2] : [y_position > y_desired]
  Motor_Moving_CW -> Motor_Moving_CCW1 [order 2] : [y_position < y_desired]
  Motor_Moving_CCW1 -> Motor_Moving_CW [order 2] : [y_position > y_desired]
  data: y_position input; y_desired input; y_motor output uint8; y_dir output uint8; steps output single
